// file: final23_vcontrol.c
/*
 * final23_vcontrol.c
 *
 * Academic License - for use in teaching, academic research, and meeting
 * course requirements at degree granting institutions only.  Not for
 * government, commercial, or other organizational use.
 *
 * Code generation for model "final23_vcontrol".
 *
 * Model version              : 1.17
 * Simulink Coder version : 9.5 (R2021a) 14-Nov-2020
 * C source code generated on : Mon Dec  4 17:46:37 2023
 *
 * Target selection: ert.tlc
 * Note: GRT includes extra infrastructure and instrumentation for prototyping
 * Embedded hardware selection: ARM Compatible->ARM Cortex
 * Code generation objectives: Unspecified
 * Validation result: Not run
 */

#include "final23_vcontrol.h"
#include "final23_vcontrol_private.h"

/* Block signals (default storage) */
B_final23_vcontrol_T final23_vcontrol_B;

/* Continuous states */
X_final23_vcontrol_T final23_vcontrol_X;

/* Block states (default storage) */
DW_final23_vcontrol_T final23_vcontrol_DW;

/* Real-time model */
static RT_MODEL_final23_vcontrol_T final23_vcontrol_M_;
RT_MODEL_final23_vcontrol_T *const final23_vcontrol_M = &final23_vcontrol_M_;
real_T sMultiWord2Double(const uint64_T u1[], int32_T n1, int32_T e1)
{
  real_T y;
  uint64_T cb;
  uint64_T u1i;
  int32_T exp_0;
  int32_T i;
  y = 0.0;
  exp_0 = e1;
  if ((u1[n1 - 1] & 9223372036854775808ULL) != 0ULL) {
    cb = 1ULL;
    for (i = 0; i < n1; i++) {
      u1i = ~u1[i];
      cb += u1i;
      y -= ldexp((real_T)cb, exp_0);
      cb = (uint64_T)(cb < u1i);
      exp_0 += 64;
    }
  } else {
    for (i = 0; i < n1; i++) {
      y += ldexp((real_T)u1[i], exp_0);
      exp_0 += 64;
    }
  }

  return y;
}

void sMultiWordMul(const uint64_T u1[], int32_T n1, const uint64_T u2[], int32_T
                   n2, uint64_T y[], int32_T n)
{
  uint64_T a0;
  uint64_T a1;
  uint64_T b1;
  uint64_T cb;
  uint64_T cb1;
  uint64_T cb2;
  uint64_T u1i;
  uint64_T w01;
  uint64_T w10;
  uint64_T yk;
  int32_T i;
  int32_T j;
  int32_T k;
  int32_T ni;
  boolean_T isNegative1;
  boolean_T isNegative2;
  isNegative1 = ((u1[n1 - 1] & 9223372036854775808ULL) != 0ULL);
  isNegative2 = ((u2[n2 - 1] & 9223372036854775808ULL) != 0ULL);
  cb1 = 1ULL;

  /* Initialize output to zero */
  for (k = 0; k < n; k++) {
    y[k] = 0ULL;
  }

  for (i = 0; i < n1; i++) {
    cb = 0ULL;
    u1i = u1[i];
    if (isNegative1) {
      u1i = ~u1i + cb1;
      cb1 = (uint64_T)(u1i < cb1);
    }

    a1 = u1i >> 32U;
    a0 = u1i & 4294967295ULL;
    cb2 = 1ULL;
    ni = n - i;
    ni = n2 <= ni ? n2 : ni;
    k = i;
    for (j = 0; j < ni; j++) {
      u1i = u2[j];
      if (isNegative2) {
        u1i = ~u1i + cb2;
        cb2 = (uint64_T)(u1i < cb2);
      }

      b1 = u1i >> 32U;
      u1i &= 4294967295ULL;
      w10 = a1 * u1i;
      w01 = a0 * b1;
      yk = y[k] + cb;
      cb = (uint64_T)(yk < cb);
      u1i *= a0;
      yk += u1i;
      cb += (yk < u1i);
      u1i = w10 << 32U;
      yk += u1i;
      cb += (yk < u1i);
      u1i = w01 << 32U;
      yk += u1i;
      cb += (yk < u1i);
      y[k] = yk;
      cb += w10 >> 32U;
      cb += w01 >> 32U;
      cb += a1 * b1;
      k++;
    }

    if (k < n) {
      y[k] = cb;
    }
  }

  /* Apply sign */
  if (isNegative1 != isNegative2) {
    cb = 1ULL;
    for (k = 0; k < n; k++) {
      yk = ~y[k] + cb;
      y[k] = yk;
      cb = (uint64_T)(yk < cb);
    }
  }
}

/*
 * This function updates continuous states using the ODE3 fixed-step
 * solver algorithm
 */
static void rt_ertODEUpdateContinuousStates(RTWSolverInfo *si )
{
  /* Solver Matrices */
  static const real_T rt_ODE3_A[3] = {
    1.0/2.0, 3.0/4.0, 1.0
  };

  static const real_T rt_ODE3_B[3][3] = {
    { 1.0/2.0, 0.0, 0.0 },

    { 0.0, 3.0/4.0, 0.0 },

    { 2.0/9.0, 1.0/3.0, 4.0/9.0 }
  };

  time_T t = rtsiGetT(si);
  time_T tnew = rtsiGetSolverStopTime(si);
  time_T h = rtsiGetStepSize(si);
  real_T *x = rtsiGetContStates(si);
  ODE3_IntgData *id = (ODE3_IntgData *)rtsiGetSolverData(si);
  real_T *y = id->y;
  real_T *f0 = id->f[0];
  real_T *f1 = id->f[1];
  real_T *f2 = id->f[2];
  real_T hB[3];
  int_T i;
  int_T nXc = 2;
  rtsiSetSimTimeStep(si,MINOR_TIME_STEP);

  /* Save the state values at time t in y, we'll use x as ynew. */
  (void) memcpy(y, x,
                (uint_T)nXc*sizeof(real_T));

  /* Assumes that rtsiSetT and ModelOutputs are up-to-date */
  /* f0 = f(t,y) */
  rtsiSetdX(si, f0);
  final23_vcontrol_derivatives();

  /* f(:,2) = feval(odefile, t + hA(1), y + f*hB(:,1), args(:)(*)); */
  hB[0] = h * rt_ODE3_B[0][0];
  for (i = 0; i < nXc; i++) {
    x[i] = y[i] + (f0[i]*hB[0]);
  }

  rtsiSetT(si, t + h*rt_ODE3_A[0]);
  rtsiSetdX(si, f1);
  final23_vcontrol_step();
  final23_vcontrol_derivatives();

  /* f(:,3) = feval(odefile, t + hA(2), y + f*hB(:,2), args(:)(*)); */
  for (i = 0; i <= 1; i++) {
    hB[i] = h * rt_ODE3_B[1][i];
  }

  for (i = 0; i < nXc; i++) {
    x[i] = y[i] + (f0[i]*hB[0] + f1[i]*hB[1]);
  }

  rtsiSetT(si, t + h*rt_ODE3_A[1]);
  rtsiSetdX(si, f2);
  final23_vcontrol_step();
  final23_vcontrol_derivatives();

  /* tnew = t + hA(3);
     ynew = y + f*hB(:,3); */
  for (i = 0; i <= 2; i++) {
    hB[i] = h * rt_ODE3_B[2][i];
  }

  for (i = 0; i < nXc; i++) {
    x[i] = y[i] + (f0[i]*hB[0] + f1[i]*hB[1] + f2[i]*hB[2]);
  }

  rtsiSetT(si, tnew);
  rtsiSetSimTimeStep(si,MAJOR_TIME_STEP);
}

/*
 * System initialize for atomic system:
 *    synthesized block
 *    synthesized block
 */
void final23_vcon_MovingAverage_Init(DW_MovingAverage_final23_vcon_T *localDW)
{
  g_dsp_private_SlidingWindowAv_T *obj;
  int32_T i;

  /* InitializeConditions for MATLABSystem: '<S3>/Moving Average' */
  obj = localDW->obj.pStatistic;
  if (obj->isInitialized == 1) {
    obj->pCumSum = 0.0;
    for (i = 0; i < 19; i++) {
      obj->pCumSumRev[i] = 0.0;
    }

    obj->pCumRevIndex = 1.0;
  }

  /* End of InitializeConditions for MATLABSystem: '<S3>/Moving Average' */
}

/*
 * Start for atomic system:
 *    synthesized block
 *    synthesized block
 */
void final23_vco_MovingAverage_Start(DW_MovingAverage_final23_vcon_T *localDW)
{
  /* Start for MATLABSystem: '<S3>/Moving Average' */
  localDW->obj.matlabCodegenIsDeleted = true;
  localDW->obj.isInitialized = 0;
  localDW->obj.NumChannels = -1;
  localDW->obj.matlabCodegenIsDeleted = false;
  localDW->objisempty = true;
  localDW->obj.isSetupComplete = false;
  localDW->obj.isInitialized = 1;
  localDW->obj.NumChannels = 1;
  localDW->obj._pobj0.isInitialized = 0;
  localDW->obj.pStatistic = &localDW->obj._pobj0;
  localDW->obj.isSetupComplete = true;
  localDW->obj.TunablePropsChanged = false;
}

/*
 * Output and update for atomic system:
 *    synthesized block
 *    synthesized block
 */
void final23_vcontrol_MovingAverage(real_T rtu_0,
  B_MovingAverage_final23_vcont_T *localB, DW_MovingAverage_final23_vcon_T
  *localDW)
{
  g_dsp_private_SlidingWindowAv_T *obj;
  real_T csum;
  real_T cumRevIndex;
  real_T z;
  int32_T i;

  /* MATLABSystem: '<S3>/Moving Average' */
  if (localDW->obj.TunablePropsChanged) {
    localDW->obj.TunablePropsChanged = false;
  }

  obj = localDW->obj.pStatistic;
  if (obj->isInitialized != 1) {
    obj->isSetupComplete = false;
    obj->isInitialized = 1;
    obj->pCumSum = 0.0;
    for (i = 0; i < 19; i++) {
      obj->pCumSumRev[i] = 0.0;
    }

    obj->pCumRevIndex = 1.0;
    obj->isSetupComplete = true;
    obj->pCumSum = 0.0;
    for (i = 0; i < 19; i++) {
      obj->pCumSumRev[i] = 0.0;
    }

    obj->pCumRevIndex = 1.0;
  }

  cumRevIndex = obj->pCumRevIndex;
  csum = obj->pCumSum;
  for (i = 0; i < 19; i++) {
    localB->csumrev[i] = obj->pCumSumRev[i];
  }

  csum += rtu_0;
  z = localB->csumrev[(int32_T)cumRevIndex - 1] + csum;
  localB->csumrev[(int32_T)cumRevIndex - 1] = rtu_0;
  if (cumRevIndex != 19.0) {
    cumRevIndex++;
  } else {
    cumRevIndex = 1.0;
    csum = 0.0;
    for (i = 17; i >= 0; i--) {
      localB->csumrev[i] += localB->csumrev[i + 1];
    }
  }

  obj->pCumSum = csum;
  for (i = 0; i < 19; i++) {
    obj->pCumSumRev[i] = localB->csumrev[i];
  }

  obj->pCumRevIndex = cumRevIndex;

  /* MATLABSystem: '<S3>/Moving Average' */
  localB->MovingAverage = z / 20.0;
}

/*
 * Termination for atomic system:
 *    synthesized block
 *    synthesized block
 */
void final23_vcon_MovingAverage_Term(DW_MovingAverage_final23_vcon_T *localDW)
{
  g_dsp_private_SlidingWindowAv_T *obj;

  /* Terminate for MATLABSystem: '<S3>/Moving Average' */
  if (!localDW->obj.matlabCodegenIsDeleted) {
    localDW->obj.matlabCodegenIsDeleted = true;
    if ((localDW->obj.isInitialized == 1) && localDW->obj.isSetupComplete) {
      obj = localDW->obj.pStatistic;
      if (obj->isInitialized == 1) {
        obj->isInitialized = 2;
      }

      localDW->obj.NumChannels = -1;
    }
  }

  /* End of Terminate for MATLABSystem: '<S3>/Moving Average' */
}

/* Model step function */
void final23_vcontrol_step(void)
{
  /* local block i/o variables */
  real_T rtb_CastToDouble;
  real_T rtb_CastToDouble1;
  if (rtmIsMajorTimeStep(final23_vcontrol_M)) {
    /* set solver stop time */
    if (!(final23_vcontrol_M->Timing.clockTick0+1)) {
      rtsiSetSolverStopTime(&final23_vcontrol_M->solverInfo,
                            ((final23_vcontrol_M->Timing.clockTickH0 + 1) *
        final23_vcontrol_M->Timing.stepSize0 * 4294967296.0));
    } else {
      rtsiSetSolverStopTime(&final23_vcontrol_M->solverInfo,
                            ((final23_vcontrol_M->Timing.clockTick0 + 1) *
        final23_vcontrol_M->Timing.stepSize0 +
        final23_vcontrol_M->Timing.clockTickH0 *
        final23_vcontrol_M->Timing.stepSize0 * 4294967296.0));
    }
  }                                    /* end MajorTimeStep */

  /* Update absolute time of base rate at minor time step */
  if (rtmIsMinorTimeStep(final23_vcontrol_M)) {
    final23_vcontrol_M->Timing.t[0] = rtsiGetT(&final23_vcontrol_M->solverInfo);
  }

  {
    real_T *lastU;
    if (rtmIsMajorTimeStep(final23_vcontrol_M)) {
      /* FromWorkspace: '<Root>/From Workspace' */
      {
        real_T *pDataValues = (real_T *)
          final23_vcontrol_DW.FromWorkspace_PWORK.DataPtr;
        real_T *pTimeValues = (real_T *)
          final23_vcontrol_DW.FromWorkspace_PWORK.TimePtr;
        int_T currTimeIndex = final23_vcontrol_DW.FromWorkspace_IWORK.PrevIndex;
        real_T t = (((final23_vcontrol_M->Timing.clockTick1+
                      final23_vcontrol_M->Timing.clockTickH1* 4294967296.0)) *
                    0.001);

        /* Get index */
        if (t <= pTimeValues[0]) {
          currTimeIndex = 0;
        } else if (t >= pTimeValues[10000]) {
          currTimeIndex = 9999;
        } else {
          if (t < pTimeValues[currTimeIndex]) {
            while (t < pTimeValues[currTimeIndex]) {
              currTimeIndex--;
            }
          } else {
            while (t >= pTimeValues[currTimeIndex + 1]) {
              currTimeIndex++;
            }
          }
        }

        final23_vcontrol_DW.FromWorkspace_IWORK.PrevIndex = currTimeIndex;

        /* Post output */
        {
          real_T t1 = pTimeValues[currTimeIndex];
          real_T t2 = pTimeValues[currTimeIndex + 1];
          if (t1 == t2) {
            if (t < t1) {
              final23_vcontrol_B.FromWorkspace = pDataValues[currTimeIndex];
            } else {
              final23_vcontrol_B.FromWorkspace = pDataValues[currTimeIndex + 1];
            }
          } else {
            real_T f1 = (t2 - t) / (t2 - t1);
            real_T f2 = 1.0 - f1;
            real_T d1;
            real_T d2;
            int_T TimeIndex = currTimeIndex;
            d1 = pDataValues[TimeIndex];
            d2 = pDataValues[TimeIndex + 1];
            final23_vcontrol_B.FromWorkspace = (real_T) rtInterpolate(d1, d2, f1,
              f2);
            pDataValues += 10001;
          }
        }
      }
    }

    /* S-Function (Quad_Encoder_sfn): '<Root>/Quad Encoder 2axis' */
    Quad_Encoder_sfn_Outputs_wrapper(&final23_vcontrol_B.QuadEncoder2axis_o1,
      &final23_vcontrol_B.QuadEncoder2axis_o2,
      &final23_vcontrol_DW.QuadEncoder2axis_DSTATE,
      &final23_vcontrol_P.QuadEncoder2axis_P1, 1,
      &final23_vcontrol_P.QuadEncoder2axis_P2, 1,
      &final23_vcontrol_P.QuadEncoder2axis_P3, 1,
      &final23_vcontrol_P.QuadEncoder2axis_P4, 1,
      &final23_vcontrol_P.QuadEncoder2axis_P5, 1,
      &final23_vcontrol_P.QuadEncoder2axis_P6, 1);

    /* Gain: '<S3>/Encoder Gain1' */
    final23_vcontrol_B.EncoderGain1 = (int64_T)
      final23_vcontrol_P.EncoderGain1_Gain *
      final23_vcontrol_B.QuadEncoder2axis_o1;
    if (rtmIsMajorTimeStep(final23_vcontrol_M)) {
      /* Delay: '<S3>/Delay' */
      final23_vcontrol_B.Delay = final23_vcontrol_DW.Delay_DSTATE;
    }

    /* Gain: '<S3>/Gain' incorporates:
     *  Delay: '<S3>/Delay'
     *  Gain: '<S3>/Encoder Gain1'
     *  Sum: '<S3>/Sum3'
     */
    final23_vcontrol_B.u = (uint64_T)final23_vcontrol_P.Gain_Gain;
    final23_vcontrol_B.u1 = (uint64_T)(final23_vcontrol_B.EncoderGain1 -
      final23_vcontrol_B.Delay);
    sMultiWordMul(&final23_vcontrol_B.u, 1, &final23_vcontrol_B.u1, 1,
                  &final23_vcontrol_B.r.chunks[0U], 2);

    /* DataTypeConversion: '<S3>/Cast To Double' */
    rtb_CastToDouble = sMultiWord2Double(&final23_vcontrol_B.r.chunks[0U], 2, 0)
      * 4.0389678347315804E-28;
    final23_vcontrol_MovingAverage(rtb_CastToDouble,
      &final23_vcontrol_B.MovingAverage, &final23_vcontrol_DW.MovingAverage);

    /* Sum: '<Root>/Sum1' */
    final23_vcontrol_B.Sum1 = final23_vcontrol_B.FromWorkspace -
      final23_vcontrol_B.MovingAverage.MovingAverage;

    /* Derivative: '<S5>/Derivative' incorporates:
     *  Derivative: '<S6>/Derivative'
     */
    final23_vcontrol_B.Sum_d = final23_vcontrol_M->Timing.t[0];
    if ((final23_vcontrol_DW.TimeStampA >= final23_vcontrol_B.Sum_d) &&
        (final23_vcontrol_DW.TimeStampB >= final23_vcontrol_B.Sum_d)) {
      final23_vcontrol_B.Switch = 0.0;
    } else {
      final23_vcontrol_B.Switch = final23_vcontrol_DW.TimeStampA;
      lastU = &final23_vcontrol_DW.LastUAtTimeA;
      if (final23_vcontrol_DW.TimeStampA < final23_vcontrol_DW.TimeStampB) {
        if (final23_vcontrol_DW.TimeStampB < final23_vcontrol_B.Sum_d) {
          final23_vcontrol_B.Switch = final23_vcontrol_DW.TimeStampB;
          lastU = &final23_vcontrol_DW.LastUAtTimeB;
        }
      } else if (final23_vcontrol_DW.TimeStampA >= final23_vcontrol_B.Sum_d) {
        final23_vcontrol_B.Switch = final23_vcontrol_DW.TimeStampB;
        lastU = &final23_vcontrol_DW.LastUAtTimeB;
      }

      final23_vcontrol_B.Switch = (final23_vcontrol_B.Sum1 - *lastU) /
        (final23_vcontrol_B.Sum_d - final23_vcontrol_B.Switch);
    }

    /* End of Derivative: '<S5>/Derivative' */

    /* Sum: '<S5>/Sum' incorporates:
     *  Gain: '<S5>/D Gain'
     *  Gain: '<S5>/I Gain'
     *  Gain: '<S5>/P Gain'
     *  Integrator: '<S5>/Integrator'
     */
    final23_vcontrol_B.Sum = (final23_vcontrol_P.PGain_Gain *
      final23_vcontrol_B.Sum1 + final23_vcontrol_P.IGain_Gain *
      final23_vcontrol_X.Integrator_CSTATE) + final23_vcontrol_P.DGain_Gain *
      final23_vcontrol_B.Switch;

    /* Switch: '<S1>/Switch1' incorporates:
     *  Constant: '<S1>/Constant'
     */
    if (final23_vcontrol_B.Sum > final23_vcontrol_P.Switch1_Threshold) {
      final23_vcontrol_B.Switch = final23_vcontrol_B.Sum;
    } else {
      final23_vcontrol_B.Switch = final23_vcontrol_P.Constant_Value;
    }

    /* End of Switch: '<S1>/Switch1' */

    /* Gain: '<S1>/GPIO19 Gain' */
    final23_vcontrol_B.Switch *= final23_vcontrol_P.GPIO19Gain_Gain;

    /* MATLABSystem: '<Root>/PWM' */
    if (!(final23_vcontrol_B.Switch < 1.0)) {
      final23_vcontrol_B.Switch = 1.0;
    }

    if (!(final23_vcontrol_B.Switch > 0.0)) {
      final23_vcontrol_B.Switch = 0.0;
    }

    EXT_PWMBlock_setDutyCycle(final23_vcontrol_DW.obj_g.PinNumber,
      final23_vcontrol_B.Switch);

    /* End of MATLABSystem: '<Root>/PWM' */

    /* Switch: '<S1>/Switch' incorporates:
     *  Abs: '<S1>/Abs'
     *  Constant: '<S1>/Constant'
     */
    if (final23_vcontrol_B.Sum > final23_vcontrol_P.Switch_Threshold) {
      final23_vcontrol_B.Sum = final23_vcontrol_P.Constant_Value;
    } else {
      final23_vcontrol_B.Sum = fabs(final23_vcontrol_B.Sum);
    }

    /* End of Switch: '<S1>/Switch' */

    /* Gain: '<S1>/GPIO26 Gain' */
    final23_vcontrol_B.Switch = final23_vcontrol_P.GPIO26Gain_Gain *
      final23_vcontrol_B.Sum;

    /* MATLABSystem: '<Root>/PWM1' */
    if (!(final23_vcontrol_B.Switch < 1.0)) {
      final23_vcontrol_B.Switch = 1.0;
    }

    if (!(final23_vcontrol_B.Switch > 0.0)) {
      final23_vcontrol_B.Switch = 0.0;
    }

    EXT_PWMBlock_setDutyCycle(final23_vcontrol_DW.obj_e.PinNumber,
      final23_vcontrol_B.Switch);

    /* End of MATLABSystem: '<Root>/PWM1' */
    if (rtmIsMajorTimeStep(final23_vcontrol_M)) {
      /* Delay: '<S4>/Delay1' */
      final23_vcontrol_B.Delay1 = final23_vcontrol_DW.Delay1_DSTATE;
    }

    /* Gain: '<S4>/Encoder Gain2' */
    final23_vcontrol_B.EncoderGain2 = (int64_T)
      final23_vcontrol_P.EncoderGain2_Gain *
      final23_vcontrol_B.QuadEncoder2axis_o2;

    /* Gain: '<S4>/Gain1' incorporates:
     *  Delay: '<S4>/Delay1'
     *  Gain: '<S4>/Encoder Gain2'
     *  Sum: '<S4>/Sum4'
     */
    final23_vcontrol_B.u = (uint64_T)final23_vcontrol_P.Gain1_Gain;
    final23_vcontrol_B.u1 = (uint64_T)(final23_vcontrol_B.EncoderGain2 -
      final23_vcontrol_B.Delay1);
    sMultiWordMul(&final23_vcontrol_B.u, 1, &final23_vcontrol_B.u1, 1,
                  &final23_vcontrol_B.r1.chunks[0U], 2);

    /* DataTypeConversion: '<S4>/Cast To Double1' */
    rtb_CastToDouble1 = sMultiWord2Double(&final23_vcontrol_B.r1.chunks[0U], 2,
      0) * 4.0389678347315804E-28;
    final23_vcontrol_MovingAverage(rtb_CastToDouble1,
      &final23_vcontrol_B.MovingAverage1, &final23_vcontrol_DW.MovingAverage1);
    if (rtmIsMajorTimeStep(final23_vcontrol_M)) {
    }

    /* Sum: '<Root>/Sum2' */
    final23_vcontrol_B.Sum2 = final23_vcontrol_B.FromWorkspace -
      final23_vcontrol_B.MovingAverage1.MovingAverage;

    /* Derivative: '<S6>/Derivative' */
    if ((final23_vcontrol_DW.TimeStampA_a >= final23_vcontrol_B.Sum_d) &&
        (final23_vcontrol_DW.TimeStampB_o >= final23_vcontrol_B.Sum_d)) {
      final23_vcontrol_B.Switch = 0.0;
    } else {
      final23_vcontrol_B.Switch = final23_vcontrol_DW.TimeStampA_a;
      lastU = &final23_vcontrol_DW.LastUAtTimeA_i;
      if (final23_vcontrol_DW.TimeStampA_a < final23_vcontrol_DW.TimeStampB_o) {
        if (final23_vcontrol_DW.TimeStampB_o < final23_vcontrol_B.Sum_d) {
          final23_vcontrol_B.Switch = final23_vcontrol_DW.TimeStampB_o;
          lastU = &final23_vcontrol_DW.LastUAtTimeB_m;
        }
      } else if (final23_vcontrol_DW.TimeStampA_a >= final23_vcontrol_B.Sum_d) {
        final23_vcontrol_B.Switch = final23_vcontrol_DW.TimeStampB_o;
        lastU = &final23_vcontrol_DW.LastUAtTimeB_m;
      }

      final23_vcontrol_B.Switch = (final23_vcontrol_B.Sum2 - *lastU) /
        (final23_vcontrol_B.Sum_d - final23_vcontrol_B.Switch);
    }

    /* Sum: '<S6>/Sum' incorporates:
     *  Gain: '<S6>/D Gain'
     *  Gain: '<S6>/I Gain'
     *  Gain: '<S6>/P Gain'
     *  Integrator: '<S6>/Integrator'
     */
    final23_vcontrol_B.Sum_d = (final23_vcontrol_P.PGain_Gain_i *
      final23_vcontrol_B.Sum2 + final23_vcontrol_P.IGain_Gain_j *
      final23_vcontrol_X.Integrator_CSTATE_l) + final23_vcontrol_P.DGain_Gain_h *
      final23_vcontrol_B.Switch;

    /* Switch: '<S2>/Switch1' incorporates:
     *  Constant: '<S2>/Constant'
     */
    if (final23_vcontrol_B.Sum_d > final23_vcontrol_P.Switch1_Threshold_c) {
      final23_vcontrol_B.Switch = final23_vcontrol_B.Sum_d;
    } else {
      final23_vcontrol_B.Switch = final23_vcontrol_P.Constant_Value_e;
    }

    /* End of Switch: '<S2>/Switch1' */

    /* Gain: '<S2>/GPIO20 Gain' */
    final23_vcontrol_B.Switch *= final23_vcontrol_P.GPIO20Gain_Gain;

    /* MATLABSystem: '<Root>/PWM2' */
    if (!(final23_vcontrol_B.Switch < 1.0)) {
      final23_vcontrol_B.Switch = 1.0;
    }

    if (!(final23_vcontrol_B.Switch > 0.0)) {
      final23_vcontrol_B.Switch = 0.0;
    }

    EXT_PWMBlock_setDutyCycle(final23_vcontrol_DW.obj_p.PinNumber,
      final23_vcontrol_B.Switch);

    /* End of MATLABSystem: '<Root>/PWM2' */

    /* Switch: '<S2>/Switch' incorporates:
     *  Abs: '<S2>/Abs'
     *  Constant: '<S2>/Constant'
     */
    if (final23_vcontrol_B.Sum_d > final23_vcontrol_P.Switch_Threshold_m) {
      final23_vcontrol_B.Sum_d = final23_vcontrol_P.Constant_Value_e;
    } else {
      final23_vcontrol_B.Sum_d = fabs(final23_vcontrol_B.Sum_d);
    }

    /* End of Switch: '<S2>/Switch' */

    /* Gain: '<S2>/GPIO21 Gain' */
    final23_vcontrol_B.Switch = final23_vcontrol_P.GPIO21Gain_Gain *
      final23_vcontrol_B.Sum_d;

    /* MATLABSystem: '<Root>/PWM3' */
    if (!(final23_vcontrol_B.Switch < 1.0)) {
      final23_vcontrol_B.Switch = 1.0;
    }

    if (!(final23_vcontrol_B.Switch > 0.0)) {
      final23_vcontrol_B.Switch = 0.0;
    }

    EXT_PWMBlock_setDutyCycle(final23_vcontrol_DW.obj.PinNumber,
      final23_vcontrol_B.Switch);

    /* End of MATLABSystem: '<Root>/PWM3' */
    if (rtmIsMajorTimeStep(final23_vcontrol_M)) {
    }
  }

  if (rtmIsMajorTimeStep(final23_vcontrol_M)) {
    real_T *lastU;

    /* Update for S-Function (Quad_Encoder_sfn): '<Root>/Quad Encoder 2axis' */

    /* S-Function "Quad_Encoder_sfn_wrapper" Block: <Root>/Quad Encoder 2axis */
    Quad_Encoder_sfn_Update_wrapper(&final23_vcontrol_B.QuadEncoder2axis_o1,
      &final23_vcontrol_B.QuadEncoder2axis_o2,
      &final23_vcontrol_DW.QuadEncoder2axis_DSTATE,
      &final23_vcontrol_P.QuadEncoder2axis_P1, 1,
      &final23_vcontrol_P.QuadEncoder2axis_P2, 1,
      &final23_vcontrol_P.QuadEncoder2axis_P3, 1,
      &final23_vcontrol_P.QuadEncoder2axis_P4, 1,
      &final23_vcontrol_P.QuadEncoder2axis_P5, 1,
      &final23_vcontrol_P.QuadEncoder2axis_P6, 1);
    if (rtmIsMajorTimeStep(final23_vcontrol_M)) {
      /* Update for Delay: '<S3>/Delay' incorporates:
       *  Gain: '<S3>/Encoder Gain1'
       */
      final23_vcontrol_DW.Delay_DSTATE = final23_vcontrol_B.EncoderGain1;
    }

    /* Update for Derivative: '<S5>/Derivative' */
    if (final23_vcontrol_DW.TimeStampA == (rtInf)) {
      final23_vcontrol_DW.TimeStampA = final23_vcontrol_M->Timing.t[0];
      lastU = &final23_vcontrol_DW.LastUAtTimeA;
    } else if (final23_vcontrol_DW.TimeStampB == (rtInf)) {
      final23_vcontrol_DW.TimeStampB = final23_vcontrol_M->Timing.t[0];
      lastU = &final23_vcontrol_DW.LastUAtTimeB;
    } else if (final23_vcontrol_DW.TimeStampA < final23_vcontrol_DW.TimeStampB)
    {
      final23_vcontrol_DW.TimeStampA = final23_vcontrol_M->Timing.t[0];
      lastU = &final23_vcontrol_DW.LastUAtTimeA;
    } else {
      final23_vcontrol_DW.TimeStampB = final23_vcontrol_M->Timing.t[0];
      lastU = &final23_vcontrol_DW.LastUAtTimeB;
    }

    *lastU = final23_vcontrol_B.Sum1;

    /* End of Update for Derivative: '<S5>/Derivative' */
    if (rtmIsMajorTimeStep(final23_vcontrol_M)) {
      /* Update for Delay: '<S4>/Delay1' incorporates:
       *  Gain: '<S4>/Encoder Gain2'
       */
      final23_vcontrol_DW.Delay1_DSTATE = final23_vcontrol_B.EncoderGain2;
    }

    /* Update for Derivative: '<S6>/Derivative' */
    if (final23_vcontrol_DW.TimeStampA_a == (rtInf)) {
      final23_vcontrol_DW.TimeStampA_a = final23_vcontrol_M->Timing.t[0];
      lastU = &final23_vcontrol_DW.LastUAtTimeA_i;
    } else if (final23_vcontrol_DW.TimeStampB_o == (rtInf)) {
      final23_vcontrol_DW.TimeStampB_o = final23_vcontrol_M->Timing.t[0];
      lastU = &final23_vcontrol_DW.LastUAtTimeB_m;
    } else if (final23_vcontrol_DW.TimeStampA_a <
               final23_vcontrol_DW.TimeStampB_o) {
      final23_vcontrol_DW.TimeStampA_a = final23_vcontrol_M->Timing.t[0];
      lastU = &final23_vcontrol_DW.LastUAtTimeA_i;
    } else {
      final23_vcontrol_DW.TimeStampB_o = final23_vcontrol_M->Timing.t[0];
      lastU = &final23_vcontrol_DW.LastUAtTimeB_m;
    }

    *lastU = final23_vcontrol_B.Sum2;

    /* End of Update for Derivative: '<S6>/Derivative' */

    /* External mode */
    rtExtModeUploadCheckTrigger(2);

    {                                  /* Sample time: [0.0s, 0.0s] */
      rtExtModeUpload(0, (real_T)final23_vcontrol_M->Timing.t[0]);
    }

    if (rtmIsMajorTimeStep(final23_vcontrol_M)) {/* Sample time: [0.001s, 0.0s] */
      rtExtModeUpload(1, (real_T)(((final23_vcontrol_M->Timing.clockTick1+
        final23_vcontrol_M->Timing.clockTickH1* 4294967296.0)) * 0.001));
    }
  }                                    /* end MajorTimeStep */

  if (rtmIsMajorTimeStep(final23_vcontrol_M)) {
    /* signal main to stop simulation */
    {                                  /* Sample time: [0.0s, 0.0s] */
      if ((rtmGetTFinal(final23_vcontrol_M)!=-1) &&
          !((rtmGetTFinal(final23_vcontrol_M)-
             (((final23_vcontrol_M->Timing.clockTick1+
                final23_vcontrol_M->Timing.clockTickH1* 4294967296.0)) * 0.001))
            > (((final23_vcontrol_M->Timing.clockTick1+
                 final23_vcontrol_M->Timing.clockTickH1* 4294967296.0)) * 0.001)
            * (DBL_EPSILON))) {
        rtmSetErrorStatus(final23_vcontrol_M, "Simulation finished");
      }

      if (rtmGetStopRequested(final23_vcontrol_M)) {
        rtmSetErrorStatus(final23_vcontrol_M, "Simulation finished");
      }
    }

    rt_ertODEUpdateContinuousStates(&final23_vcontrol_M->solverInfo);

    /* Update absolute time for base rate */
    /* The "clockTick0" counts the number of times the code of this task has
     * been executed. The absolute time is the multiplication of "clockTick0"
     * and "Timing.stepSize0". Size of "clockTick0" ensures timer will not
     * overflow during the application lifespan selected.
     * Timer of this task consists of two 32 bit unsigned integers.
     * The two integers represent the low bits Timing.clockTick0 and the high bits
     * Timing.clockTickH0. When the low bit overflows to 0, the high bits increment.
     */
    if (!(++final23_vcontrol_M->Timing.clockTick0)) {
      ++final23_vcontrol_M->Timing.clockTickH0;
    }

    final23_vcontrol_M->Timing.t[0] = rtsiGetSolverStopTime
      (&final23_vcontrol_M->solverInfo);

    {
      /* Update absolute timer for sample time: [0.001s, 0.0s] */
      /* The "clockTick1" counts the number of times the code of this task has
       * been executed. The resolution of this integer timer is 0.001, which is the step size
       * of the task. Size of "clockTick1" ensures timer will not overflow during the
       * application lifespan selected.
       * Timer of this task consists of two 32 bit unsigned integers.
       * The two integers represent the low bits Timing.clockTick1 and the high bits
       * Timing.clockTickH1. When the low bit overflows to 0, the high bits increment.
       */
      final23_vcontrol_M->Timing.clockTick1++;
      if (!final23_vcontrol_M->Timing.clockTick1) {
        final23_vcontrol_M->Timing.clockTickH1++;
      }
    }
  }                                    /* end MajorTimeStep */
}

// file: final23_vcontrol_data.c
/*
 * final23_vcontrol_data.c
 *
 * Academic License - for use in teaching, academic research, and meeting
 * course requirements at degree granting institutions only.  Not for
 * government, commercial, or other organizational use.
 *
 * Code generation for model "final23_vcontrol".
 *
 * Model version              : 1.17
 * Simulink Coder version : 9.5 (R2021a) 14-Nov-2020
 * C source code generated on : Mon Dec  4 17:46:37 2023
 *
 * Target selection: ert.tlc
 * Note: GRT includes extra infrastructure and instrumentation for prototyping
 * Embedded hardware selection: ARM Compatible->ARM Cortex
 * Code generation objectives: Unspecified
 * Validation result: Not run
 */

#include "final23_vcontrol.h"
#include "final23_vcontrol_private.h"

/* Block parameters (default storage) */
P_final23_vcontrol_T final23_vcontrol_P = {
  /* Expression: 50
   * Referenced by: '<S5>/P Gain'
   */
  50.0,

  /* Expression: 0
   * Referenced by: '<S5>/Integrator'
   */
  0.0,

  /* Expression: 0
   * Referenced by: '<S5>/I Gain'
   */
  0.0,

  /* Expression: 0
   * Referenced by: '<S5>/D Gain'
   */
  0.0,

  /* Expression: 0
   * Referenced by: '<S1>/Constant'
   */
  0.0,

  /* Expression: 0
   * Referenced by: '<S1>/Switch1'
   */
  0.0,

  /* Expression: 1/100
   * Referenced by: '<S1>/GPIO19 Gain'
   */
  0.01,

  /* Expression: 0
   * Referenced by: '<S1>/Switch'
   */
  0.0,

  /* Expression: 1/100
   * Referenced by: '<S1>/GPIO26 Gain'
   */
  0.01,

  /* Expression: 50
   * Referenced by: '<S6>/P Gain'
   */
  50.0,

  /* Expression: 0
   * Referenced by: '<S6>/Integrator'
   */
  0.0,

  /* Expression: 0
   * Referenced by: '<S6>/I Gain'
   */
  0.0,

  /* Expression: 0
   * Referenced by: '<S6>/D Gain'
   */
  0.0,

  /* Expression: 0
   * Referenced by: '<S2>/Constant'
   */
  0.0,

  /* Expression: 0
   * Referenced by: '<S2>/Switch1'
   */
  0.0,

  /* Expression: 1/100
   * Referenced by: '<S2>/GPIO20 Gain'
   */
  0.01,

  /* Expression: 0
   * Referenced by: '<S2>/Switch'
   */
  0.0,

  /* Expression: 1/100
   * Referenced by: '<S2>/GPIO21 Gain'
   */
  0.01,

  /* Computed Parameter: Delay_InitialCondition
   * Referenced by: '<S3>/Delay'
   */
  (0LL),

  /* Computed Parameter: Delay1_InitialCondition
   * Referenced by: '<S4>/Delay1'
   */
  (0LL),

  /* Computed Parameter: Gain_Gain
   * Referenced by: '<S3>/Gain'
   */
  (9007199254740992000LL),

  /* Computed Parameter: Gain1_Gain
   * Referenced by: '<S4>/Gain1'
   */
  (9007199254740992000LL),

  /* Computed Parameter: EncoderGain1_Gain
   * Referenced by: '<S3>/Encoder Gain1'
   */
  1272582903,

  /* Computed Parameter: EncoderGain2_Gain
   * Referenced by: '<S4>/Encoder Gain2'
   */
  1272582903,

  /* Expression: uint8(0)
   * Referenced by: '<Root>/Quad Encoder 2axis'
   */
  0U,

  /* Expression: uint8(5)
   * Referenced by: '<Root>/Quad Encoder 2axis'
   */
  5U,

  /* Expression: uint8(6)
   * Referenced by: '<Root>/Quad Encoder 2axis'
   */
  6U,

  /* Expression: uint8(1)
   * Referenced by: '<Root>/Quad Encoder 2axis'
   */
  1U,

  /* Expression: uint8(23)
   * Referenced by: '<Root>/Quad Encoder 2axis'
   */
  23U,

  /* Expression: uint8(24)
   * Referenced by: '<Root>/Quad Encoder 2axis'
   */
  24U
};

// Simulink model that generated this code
simulink model "final23_vcontrol"  (R2021a)
settings: Solver=FixedStepAuto  StartTime=0.0  StopTime=inf  FixedStep=0.001  RelTol=1e-3  EnableMultiTasking=on
StopFcn:
  | mypi=raspi();
  | writeDigitalPin(mypi,19,0);
  | writeDigitalPin(mypi,26,0);
  | writeDigitalPin(mypi,20,0);
  | writeDigitalPin(mypi,21,0);
  | clear mypi;
libraries: raspberrypiBasiclib x4

== system final23_vcontrol ==
  note: Encoder Position (To Workspace)
  Delay : Delay  DelayLength=1
  Delay1 : Delay  DelayLength=1
  Encoder Gain1 : Gain  Gain=1/216
  Encoder Gain2 : Gain  Gain=1/216
  From Workspace : FromWorkspace  VariableName=simin  SampleTime=0.001
  Gain : Gain  Gain=1000
  Gain1 : Gain  Gain=1000
  Motor Subsystem : Subsystem
  Motor Subsystem1 : Subsystem
  PID Subsystem : Subsystem
  PID Subsystem1 : Subsystem
  PWM : raspberrypiBasiclib/PWM  board=Pi 4 Model B  Pin_=19  Frequency=1000  blockPlatform=Raspberry Pi
  PWM1 : raspberrypiBasiclib/PWM  board=Pi 4 Model B  Pin_=26  Frequency=1000  blockPlatform=Raspberry Pi
  PWM2 : raspberrypiBasiclib/PWM  board=Pi 4 Model B  Pin_=20  Frequency=1000  blockPlatform=Raspberry Pi
  PWM3 : raspberrypiBasiclib/PWM  board=Pi 4 Model B  Pin_=21  Frequency=1000  blockPlatform=Raspberry Pi
  Quad Encoder 2axis : S-Function  InitFcn=try, set_param(gcb,'FunctionName','Quad_Encoder_sfn'), end  FunctionName=Quad_Encoder_sfn  Parameters=uint8(0),uint8(5),uint8(6),uint8(1),uint8(23),uint8(24)  SFunctionModules=Quad_Encoder_sfn_wrapper  SFunctionDeploymentMode=off  EnableBusSupport=off  mask(S-Function Builder){}
      mask init:
      | val = [[.9  0.75 0.75 1 1 .9 .9 1]',[1 1 0.75 0.75 .9 .9 1 .9]'];try , sys = get_param(gcb,'SfunBuilderFcnName');if isempty(sys), sys = get_param(gcb,'FunctionName'); end,catch, sys = get_param(gcb,'FunctionName'); end
  Sum1 : Sum  Inputs=|+-
  Sum2 : Sum  Inputs=-+|
  Sum3 : Sum  Inputs=|+-
  Sum4 : Sum  Inputs=|+-
  To Workspace : ToWorkspace  VariableName=controled_position  SaveFormat=Structure With Time  SampleTime=0.001
  wires:
  Quad Encoder 2axis/1 -> Encoder Gain1/1
  Quad Encoder 2axis/2 -> Encoder Gain2/1
  Encoder Gain1/1 -> Delay/1, Sum3/1
  Sum1/1 -> PID Subsystem/1(In1)
  PID Subsystem/1(Out1) -> Motor Subsystem/1(In1)
  Motor Subsystem/1(Out1) -> PWM/1
  Motor Subsystem/2(Out2) -> PWM1/1
  Motor Subsystem1/2(Out2) -> PWM3/1
  Motor Subsystem1/1(Out1) -> PWM2/1
  PID Subsystem1/1(Out1) -> Motor Subsystem1/1(In1)
  Sum2/1 -> PID Subsystem1/1(In1)
  From Workspace/1 -> Sum1/1, Sum2/2
  Encoder Gain2/1 -> Delay1/1, Sum4/1
  Delay/1 -> Sum3/2
  Sum3/1 -> Gain/1
  Sum4/1 -> Gain1/1
  Delay1/1 -> Sum4/2

== system final23_vcontrol/Motor Subsystem ==
  In1 : Inport
  Abs : Abs
  Constant : Constant  Value=0
  GPIO19 Gain : Gain  Gain=1/100
  GPIO26 Gain : Gain  Gain=1/100
  Switch : Switch  Criteria=u2 > Threshold
  Switch1 : Switch  Criteria=u2 > Threshold
  Out1 : Outport
  Out2 : Outport  Port=2
  wires:
  Switch/1 -> GPIO26 Gain/1
  Abs/1 -> Switch/3
  Switch1/1 -> GPIO19 Gain/1
  In1/1 -> Abs/1, Switch/2, Switch1/1, Switch1/2
  Constant/1 -> Switch/1, Switch1/3
  GPIO26 Gain/1 -> Out2/1
  GPIO19 Gain/1 -> Out1/1

== system final23_vcontrol/Motor Subsystem1 ==
  In1 : Inport
  Abs : Abs
  Constant : Constant  Value=0
  GPIO20 Gain : Gain  Gain=1/100
  GPIO21 Gain : Gain  Gain=1/100
  Switch : Switch  Criteria=u2 > Threshold
  Switch1 : Switch  Criteria=u2 > Threshold
  Out1 : Outport
  Out2 : Outport  Port=2
  wires:
  Switch/1 -> GPIO21 Gain/1
  Abs/1 -> Switch/3
  Switch1/1 -> GPIO20 Gain/1
  In1/1 -> Abs/1, Switch/2, Switch1/1, Switch1/2
  Constant/1 -> Switch/1, Switch1/3
  GPIO21 Gain/1 -> Out2/1
  GPIO20 Gain/1 -> Out1/1

== system final23_vcontrol/PID Subsystem ==
  In1 : Inport
  D Gain : Gain  Gain=0
  Derivative : Derivative
  I Gain : Gain  Gain=0
  Integrator : Integrator
  P Gain : Gain  Gain=50
  Sum : Sum  Inputs=+++
  Out1 : Outport
  wires:
  Derivative/1 -> D Gain/1
  I Gain/1 -> Sum/2
  Integrator/1 -> I Gain/1
  P Gain/1 -> Sum/1
  D Gain/1 -> Sum/3
  Sum/1 -> Out1/1
  In1/1 -> P Gain/1, Derivative/1, Integrator/1

== system final23_vcontrol/PID Subsystem1 ==
  In1 : Inport
  D Gain : Gain  Gain=0
  Derivative : Derivative
  I Gain : Gain  Gain=0
  Integrator : Integrator
  P Gain : Gain  Gain=50
  Sum : Sum  Inputs=+++
  Out1 : Outport
  wires:
  Derivative/1 -> D Gain/1
  I Gain/1 -> Sum/2
  Integrator/1 -> I Gain/1
  P Gain/1 -> Sum/1
  D Gain/1 -> Sum/3
  Sum/1 -> Out1/1
  In1/1 -> P Gain/1, Derivative/1, Integrator/1
